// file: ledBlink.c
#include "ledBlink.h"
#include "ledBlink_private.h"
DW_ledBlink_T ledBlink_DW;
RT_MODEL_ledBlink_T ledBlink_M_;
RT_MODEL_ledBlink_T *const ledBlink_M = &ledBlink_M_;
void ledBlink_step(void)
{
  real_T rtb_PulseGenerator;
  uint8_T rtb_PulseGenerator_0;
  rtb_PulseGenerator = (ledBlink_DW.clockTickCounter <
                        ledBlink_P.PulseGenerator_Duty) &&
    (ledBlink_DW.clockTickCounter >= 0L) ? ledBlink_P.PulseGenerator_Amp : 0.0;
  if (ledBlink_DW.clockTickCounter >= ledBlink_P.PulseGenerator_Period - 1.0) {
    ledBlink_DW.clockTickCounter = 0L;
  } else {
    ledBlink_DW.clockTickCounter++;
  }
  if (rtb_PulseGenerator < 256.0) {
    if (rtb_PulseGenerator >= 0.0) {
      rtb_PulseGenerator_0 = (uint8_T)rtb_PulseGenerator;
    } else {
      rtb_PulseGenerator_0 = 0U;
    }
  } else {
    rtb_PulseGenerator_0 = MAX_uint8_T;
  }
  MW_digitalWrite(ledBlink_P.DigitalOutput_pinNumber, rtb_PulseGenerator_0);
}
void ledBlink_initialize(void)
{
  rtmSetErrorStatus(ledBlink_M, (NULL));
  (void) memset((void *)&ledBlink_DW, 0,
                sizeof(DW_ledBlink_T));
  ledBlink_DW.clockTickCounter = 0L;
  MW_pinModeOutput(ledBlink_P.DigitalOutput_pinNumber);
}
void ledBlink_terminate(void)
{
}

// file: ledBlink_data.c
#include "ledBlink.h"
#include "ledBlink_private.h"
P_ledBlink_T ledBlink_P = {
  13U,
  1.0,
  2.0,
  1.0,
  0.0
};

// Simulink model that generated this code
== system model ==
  DigitalOutput : arduinolib/Digital Output  pinNumber=13  <- 1: PulseGenerator
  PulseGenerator : DiscretePulseGenerator  PulseWidth=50
